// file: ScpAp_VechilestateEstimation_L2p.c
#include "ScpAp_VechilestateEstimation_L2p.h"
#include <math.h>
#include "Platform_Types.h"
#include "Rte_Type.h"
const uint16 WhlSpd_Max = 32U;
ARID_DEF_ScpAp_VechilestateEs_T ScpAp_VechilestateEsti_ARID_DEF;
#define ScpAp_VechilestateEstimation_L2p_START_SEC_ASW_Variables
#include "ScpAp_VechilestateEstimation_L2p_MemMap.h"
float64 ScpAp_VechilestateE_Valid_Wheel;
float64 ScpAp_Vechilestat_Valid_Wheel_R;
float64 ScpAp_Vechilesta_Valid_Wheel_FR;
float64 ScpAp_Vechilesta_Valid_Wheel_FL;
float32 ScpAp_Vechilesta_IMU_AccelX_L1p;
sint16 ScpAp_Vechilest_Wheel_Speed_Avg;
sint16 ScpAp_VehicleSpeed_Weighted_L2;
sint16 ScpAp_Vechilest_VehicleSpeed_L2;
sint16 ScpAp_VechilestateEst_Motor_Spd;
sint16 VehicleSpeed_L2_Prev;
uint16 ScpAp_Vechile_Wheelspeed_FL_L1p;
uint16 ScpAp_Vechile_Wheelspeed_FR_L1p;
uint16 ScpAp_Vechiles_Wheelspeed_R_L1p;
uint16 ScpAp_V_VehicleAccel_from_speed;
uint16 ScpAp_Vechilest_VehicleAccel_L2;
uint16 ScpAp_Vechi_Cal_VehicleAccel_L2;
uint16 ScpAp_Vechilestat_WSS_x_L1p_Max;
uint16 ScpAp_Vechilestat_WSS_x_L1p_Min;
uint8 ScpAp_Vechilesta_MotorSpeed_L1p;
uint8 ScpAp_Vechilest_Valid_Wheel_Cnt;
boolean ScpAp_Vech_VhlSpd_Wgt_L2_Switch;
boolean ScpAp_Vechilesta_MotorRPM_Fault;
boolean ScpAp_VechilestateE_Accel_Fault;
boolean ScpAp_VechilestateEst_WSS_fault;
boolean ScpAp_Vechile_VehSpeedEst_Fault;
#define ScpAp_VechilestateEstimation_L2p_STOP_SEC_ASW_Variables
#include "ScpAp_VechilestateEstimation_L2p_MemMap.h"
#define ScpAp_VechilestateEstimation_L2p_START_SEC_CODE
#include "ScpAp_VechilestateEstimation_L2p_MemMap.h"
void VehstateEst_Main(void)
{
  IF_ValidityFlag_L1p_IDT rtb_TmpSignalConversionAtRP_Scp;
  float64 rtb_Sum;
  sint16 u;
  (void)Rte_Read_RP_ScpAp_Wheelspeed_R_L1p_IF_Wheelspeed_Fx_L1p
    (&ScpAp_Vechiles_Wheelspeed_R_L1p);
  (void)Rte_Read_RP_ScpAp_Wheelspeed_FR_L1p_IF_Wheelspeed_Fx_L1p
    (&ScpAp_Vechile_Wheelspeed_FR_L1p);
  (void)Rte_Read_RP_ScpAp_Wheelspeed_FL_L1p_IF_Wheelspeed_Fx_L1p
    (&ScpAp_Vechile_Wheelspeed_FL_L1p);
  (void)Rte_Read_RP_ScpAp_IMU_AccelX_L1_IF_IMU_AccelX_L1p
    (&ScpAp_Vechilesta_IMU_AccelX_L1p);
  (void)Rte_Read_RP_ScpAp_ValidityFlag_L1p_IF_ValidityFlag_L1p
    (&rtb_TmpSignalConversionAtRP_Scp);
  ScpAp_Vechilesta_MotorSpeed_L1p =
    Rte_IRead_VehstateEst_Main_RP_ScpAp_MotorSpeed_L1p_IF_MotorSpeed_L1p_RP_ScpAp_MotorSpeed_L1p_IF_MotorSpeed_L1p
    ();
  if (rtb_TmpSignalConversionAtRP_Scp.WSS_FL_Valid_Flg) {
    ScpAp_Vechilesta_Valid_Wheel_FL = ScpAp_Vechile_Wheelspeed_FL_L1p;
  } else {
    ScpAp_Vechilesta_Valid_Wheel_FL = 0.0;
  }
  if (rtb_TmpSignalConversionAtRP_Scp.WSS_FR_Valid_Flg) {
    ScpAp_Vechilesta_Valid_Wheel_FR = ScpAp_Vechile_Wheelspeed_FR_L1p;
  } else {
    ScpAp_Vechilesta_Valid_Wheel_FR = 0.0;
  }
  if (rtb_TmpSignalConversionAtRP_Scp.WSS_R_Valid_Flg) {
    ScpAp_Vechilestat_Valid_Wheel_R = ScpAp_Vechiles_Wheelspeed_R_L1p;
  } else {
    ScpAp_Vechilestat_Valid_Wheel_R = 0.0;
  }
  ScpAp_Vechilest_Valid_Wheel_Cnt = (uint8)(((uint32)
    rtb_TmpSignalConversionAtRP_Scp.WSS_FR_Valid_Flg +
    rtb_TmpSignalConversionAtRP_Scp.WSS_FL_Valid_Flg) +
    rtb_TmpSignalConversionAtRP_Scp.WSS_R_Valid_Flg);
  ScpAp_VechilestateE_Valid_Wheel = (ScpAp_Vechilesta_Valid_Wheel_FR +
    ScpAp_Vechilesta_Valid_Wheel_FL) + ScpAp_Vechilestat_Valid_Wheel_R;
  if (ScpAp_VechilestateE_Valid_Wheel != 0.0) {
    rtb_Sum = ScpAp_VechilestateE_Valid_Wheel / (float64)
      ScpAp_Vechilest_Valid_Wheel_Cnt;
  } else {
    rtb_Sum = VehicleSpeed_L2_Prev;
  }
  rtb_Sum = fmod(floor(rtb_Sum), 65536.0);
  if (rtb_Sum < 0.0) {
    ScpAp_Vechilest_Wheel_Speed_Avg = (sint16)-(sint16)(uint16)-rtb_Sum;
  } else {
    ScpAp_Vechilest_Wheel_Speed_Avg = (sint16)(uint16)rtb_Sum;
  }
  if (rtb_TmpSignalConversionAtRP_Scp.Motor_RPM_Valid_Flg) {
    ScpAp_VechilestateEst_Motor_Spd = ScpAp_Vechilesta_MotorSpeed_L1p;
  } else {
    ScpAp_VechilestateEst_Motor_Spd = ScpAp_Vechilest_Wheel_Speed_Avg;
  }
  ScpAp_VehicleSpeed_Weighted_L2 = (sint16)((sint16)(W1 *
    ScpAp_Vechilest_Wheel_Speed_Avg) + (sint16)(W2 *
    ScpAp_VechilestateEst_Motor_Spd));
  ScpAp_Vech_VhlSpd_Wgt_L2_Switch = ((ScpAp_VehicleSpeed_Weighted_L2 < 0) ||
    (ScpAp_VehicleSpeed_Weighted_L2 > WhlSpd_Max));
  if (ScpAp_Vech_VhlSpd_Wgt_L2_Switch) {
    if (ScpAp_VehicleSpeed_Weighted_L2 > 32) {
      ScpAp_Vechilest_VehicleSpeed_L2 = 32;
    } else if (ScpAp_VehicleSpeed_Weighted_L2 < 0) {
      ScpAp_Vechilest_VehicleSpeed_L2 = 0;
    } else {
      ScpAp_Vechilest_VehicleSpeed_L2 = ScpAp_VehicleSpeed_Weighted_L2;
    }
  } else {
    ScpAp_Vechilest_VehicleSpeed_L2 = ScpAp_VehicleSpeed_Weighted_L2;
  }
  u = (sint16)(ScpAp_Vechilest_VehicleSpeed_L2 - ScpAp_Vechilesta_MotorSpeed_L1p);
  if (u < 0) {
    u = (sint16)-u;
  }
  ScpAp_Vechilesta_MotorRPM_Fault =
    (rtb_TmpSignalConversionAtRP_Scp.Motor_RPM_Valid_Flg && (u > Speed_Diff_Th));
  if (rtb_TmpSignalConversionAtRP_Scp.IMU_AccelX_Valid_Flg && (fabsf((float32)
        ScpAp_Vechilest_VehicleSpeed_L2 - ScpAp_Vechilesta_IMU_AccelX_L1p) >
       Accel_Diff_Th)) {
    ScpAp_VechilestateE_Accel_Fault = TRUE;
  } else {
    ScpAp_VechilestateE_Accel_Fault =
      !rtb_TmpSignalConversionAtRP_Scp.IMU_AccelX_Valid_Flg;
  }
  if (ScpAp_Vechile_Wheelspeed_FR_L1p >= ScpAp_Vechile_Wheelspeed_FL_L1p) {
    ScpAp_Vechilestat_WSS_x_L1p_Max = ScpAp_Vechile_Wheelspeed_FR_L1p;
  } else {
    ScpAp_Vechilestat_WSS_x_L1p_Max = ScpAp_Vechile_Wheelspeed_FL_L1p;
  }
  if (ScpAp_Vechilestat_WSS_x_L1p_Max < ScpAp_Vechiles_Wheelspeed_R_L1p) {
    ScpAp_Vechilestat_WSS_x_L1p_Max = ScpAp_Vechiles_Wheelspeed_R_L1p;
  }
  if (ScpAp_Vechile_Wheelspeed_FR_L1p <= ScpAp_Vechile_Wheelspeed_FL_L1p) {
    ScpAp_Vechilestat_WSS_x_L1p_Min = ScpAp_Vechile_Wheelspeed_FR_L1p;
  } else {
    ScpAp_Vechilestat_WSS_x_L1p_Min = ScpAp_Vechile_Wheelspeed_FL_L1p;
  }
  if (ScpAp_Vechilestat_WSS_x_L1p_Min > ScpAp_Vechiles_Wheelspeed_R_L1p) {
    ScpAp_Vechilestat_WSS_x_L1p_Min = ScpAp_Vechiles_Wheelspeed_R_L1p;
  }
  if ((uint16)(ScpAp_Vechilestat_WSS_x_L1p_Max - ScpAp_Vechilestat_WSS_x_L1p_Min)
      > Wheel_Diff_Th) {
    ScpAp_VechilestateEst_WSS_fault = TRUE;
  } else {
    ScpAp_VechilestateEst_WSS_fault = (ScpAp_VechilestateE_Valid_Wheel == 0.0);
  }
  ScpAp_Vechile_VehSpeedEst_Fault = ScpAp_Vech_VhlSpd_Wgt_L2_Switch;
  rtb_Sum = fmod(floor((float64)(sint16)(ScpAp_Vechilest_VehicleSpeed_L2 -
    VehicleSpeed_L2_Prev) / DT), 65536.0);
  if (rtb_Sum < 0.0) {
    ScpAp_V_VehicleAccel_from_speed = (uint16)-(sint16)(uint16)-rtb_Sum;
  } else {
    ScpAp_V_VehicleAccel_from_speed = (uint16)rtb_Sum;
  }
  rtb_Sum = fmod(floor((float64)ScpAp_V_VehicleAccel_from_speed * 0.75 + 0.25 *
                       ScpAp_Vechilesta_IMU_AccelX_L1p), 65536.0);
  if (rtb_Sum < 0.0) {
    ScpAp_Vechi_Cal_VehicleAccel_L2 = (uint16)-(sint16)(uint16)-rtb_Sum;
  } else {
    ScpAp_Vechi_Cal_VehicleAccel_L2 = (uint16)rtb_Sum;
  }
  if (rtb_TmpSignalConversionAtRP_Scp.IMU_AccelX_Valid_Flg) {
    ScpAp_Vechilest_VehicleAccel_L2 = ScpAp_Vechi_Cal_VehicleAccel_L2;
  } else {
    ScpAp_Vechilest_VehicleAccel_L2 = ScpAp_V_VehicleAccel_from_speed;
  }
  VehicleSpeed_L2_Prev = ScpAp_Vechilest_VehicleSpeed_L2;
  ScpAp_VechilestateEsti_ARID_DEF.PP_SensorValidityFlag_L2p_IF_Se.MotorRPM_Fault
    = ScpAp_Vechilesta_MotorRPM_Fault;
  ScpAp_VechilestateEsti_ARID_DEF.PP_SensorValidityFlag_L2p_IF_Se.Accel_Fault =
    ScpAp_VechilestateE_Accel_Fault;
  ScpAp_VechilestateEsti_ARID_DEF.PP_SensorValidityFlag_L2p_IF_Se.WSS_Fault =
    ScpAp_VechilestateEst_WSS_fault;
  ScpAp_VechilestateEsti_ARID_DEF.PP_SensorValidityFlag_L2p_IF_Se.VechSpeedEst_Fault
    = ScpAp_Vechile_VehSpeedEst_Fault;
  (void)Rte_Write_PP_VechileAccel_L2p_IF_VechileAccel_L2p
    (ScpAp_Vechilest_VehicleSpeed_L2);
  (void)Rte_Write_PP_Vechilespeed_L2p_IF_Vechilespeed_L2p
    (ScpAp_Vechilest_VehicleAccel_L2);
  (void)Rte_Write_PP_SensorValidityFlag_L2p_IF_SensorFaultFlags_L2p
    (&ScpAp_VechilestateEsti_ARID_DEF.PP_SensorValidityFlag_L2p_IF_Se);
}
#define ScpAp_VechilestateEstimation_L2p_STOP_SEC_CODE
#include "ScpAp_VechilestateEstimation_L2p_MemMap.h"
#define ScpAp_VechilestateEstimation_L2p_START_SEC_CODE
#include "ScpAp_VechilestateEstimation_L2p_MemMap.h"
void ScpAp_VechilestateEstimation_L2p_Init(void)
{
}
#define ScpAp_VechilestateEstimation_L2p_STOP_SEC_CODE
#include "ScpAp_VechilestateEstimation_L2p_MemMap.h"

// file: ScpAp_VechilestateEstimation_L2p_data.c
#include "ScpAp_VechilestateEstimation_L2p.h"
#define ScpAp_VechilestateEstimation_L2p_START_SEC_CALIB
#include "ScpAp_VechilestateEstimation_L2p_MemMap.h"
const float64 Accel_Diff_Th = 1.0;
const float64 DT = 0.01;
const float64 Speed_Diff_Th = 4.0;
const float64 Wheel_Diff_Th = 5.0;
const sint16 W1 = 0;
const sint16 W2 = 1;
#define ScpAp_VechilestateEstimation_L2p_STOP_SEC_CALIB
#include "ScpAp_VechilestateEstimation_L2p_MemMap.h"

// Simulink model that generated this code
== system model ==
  RP_ScpAp_IMU_AccelX_L1_IF_IMU_AccelX_L1p : Inport
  RP_ScpAp_MotorSpeed_L1p_IF_MotorSpeed_L1p : Inport
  RP_ScpAp_ValidityFlag_L1p_IF_ValidityFlag_L1p : Inport
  RP_ScpAp_Wheelspeed_FL_L1p_IF_Wheelspeed_Fx_L1p : Inport
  RP_ScpAp_Wheelspeed_FR_L1p_IF_Wheelspeed_Fx_L1p : Inport
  RP_ScpAp_Wheelspeed_R_L1p_IF_Wheelspeed_Fx_L1p : Inport
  PP_SensorValidityFlag_L2p_IF_SensorFaultFlags_L2p : Outport  <- 1: Subsystem#1
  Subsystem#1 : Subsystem  <- 1: RP_ScpAp_IMU_AccelX_L1_IF_IMU_AccelX_L1p, 2: RP_ScpAp_MotorSpeed_L1p_IF_MotorSpeed_L1p, 3: RP_ScpAp_ValidityFlag_L1p_IF_ValidityFlag_L1p, 4: RP_ScpAp_Wheelspeed_FL_L1p_IF_Wheelspeed_Fx_L1p, 5: RP_ScpAp_Wheelspeed_FR_L1p_IF_Wheelspeed_Fx_L1p, 6: RP_ScpAp_Wheelspeed_R_L1p_IF_Wheelspeed_Fx_L1p
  PP_VechileAccel_L2p_IF_VechileAccel_L2p : Outport  <- 1: Subsystem#1/2
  PP_Vechilespeed_L2p_IF_Vechilespeed_L2p : Outport  <- 1: Subsystem#1/3
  EventListener#1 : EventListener
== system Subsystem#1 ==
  Inport#1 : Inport
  Inport#2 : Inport
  Inport#3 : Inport
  Inport#4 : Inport
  Inport#5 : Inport
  Inport#6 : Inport
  Outport#1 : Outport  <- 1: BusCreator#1
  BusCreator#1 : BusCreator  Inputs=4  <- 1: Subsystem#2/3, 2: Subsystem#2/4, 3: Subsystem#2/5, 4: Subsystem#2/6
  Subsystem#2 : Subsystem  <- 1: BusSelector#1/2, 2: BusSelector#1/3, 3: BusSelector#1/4, 4: DataTypeConversion#1, 5: DataTypeConversion#2, 6: DataTypeConversion#3, 7: DataTypeConversion#4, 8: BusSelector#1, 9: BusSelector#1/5, 10: DataTypeConversion#5
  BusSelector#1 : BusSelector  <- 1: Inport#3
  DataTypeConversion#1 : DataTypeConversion  <- 1: Inport#5
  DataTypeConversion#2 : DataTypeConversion  <- 1: Inport#4
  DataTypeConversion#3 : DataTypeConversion  <- 1: Inport#6
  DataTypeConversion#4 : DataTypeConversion  <- 1: Inport#2
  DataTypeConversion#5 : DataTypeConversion  <- 1: Inport#1
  Outport#2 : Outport  <- 1: Subsystem#2/2
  Outport#3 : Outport  <- 1: Subsystem#2
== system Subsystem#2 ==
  WSS_FR_Valid_Flg : Inport
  WSS_FL_Valid_Flg : Inport
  WSS_R_Valid_Flg : Inport
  Wheelspeed_FR_L1p : Inport
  Wheelspeed_FL_L1p : Inport
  Wheelspeed_R_L1p : Inport
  MotorSpeed_L1p : Inport
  Motor_RPM_Valid_Flg : Inport
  IMU_AccelX_Valid_Flg : Inport
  IMU_AccelX_L1p : Inport
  VehicleAccel_L2 : Outport  <- 1: Subsystem#3
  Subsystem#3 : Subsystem  <- 1: Subsystem#4, 2: UnitDelay#1, 3: IMU_AccelX_Valid_Flg, 4: IMU_AccelX_L1p
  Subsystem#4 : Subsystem  <- 1: Subsystem#5, 2: Subsystem#6
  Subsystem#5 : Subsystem  <- 1: WSS_FR_Valid_Flg, 2: WSS_FL_Valid_Flg, 3: WSS_R_Valid_Flg, 4: Wheelspeed_FR_L1p, 5: Wheelspeed_FL_L1p, 6: Wheelspeed_R_L1p, 7: UnitDelay#1
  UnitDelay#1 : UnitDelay  <- 1: Subsystem#4
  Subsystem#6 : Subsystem  <- 1: MotorSpeed_L1p, 2: Motor_RPM_Valid_Flg, 3: Subsystem#5
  VehicleSpeed_L2 : Outport  <- 1: Subsystem#4
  MotorRPM_Fault : Outport  <- 1: Subsystem#7
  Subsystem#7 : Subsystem  <- 1: Motor_RPM_Valid_Flg, 2: Subsystem#4, 3: MotorSpeed_L1p, 4: IMU_AccelX_Valid_Flg, 5: IMU_AccelX_L1p, 6: Wheelspeed_FR_L1p, 7: Wheelspeed_FL_L1p, 8: Wheelspeed_R_L1p, 9: Subsystem#4/2, 10: Subsystem#5/2
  Accel_Fault : Outport  <- 1: Subsystem#7/2
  WSS_fault : Outport  <- 1: Subsystem#7/3
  VehSpeedEst_Fault : Outport  <- 1: Subsystem#7/4
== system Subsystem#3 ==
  Inport#7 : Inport
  VehicleSpeed_L2_Prev : Inport
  Inport#8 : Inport
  Inport#9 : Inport
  Outport#4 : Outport  <- 1: Switch#1
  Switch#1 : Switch  Criteria=u2 > Threshold  <- 1: Cal_VehicleAccel_L2, 2: Inport#8, 3: DataTypeConversion#6
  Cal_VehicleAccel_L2 : Subsystem  <- 1: DataTypeConversion#6, 2: Inport#9
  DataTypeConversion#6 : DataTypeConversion  <- 1: Product#1
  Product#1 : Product  Inputs=*/  <- 1: Sum#1, 2: Constant#1
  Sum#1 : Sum  Inputs=+-  <- 1: Inport#7, 2: VehicleSpeed_L2_Prev
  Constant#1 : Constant  Value=DT
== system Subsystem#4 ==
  Wheel_Speed_Avg : Inport
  Motor_Spd : Inport
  Outport#5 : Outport  <- 1: Switch
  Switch : Switch  Criteria=u2 > Threshold  <- 1: Saturate#1, 2: Logic#1, 3: Sum
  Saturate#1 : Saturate  UpperLimit=32  LowerLimit=0  <- 1: Sum
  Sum : Sum  <- 1: Product#2, 2: Product#3
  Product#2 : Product  <- 1: Constant#2, 2: Wheel_Speed_Avg
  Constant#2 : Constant  Value=W1
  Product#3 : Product  <- 1: Constant#3, 2: Motor_Spd
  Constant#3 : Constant  Value=W2
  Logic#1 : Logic  Operator=OR  <- 1: RelationalOperator#1, 2: RelationalOperator#2
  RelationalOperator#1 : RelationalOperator  Operator=<  <- 1: Sum, 2: Constant#4
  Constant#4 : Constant  Value=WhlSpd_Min
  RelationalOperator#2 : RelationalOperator  Operator=>  <- 1: Sum, 2: Constant#5
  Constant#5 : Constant  Value=WhlSpd_Max
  VehicleSpeed_Weighted_L2 : Outport  <- 1: Sum
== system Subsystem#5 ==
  Inport#10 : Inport
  Inport#11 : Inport
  Inport#12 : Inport
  Inport#13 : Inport
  Inport#14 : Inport
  Inport#15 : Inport
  Inport#16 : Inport
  Outport#6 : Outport  <- 1: DataTypeConversion#7
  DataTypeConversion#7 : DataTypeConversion  <- 1: Switch#2
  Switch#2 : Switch  Criteria=u2 ~= 0  <- 1: Product#4, 2: Sum#2, 3: Inport#16
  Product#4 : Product  Inputs=*/  <- 1: Sum#2, 2: Subsystem#8/4
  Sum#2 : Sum  Inputs=+++  <- 1: Subsystem#8, 2: Subsystem#8/2, 3: Subsystem#8/3
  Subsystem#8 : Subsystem  <- 1: Inport#10, 2: Inport#13, 3: Inport#11, 4: Inport#14, 5: Inport#12, 6: Inport#15
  Valid_Wheel : Outport  <- 1: Sum#2
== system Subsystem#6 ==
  Inport#17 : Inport
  Inport#18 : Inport
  Inport#19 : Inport
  Outport#7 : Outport  <- 1: Switch#3
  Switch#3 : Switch  Criteria=u2 > Threshold  <- 1: Inport#17, 2: Inport#18, 3: Inport#19
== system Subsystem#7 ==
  Inport#20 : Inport
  Inport#21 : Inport
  Inport#22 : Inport
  Inport#23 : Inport
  Inport#24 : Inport
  Inport#25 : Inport
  Inport#26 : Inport
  Inport#27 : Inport
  Inport#28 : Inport
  Inport#29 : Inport
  Outport#8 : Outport  <- 1: Switch#4
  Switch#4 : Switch  Criteria=u2 > Threshold  <- 1: Constant#6, 2: Logic#2, 3: Constant#7
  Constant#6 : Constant
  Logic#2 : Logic  <- 1: RelationalOperator#3, 2: RelationalOperator#4
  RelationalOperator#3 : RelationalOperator  Operator===  <- 1: Inport#20, 2: Constant#8
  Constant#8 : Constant
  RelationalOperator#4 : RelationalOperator  Operator=>  <- 1: Abs#1, 2: Constant#9
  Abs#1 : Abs  <- 1: Sum#3
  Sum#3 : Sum  Inputs=+-  <- 1: Inport#21, 2: Inport#22
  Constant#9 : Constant  Value=Speed_Diff_Th
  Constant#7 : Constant  Value=0
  Outport#9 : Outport  <- 1: Switch#5
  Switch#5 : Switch  Criteria=u2 > Threshold  <- 1: Constant#10, 2: Logic#3, 3: Switch#6
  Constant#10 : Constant
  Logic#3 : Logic  <- 1: RelationalOperator#5, 2: RelationalOperator#6
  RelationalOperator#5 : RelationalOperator  Operator===  <- 1: Inport#23, 2: Constant#11
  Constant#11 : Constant
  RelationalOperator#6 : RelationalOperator  Operator=>  <- 1: Abs#2, 2: Constant#12
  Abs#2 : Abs  <- 1: Sum#4
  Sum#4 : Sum  Inputs=+-  <- 1: Inport#21, 2: Inport#24
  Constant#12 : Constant  Value=Accel_Diff_Th
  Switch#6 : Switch  Criteria=u2 > Threshold  <- 1: Constant#13, 2: RelationalOperator#7, 3: Constant#14
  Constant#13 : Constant
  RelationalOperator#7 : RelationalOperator  Operator===  <- 1: Inport#23, 2: Constant#15
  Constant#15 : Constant  Value=0
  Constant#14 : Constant  Value=0
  Outport#10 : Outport  <- 1: Switch#7
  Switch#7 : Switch  Criteria=u2 > Threshold  <- 1: Constant#16, 2: RelationalOperator#8, 3: Switch#8
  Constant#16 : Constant
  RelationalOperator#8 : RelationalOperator  Operator=>  <- 1: Sum#5, 2: Constant#17
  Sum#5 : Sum  Inputs=+-  <- 1: Max, 2: MinMax#1
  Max : MinMax  Function=max  Inputs=3  <- 1: Inport#25, 2: Inport#26, 3: Inport#27
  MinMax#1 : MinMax  Inputs=3  <- 1: Inport#25, 2: Inport#26, 3: Inport#27
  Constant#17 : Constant  Value=Wheel_Diff_Th
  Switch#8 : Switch  Criteria=u2 > Threshold  <- 1: Constant#18, 2: RelationalOperator#9, 3: Constant#19
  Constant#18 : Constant
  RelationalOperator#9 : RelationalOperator  Operator===  <- 1: Inport#29, 2: Constant#20
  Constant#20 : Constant  Value=0
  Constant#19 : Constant  Value=0
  Outport#11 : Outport  <- 1: Switch#9
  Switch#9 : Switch  Criteria=u2 > Threshold  <- 1: Constant#21, 2: Logic#4, 3: Constant#22
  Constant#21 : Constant
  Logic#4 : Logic  Operator=OR  <- 1: RelationalOperator#10, 2: RelationalOperator#11
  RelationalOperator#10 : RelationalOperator  Operator=<  <- 1: Inport#28, 2: Constant#23
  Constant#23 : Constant  Value=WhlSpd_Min
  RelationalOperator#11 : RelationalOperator  Operator=>  <- 1: Inport#28, 2: Constant#24
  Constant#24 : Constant  Value=WhlSpd_Max
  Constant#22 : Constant  Value=0
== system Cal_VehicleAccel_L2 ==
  VehicleAccel_from_speed : Inport
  Inport#30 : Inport
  Outport#12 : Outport  <- 1: DataTypeConversion#8
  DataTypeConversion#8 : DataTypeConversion  <- 1: Sum#6
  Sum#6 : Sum  <- 1: Product#5, 2: Product#6
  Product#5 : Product  <- 1: VehicleAccel_from_speed, 2: Constant#25
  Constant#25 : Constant  Value=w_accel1
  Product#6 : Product  <- 1: Constant#26, 2: Inport#30
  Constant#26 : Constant  Value=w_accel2
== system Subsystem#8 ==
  Inport#31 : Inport
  Inport#32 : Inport
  Inport#33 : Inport
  Inport#34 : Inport
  Inport#35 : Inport
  Inport#36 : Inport
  Valid_Wheel_FR : Outport  <- 1: Subsystem#9
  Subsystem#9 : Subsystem  <- 1: Inport#31, 2: Inport#32
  Valid_Wheel_FL : Outport  <- 1: Subsystem#10
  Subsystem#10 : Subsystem  <- 1: Inport#33, 2: Inport#34
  Valid_Wheel_R : Outport  <- 1: Subsystem#11
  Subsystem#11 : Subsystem  <- 1: Inport#35, 2: Inport#36
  Valid_Wheel_Cnt : Outport  <- 1: Sum#7
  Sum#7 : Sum  Inputs=+++  <- 1: Inport#31, 2: Inport#33, 3: Inport#35
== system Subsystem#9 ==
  Inport#37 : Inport
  Inport#38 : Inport
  Outport#13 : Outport  <- 1: Switch#10
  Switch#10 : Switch  Criteria=u2 > Threshold  <- 1: Inport#38, 2: Inport#37, 3: Constant#27
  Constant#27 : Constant  Value=0
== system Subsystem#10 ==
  Inport#39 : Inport
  Inport#40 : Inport
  Outport#14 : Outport  <- 1: Switch#11
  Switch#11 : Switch  Criteria=u2 > Threshold  <- 1: Inport#40, 2: Inport#39, 3: Constant#28
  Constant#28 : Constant  Value=0
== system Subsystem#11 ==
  Inport#41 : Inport
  Inport#42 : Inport
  Outport#15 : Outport  <- 1: Switch#12
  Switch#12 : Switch  Criteria=u2 > Threshold  <- 1: Inport#42, 2: Inport#41, 3: Constant#29
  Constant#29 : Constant  Value=0
